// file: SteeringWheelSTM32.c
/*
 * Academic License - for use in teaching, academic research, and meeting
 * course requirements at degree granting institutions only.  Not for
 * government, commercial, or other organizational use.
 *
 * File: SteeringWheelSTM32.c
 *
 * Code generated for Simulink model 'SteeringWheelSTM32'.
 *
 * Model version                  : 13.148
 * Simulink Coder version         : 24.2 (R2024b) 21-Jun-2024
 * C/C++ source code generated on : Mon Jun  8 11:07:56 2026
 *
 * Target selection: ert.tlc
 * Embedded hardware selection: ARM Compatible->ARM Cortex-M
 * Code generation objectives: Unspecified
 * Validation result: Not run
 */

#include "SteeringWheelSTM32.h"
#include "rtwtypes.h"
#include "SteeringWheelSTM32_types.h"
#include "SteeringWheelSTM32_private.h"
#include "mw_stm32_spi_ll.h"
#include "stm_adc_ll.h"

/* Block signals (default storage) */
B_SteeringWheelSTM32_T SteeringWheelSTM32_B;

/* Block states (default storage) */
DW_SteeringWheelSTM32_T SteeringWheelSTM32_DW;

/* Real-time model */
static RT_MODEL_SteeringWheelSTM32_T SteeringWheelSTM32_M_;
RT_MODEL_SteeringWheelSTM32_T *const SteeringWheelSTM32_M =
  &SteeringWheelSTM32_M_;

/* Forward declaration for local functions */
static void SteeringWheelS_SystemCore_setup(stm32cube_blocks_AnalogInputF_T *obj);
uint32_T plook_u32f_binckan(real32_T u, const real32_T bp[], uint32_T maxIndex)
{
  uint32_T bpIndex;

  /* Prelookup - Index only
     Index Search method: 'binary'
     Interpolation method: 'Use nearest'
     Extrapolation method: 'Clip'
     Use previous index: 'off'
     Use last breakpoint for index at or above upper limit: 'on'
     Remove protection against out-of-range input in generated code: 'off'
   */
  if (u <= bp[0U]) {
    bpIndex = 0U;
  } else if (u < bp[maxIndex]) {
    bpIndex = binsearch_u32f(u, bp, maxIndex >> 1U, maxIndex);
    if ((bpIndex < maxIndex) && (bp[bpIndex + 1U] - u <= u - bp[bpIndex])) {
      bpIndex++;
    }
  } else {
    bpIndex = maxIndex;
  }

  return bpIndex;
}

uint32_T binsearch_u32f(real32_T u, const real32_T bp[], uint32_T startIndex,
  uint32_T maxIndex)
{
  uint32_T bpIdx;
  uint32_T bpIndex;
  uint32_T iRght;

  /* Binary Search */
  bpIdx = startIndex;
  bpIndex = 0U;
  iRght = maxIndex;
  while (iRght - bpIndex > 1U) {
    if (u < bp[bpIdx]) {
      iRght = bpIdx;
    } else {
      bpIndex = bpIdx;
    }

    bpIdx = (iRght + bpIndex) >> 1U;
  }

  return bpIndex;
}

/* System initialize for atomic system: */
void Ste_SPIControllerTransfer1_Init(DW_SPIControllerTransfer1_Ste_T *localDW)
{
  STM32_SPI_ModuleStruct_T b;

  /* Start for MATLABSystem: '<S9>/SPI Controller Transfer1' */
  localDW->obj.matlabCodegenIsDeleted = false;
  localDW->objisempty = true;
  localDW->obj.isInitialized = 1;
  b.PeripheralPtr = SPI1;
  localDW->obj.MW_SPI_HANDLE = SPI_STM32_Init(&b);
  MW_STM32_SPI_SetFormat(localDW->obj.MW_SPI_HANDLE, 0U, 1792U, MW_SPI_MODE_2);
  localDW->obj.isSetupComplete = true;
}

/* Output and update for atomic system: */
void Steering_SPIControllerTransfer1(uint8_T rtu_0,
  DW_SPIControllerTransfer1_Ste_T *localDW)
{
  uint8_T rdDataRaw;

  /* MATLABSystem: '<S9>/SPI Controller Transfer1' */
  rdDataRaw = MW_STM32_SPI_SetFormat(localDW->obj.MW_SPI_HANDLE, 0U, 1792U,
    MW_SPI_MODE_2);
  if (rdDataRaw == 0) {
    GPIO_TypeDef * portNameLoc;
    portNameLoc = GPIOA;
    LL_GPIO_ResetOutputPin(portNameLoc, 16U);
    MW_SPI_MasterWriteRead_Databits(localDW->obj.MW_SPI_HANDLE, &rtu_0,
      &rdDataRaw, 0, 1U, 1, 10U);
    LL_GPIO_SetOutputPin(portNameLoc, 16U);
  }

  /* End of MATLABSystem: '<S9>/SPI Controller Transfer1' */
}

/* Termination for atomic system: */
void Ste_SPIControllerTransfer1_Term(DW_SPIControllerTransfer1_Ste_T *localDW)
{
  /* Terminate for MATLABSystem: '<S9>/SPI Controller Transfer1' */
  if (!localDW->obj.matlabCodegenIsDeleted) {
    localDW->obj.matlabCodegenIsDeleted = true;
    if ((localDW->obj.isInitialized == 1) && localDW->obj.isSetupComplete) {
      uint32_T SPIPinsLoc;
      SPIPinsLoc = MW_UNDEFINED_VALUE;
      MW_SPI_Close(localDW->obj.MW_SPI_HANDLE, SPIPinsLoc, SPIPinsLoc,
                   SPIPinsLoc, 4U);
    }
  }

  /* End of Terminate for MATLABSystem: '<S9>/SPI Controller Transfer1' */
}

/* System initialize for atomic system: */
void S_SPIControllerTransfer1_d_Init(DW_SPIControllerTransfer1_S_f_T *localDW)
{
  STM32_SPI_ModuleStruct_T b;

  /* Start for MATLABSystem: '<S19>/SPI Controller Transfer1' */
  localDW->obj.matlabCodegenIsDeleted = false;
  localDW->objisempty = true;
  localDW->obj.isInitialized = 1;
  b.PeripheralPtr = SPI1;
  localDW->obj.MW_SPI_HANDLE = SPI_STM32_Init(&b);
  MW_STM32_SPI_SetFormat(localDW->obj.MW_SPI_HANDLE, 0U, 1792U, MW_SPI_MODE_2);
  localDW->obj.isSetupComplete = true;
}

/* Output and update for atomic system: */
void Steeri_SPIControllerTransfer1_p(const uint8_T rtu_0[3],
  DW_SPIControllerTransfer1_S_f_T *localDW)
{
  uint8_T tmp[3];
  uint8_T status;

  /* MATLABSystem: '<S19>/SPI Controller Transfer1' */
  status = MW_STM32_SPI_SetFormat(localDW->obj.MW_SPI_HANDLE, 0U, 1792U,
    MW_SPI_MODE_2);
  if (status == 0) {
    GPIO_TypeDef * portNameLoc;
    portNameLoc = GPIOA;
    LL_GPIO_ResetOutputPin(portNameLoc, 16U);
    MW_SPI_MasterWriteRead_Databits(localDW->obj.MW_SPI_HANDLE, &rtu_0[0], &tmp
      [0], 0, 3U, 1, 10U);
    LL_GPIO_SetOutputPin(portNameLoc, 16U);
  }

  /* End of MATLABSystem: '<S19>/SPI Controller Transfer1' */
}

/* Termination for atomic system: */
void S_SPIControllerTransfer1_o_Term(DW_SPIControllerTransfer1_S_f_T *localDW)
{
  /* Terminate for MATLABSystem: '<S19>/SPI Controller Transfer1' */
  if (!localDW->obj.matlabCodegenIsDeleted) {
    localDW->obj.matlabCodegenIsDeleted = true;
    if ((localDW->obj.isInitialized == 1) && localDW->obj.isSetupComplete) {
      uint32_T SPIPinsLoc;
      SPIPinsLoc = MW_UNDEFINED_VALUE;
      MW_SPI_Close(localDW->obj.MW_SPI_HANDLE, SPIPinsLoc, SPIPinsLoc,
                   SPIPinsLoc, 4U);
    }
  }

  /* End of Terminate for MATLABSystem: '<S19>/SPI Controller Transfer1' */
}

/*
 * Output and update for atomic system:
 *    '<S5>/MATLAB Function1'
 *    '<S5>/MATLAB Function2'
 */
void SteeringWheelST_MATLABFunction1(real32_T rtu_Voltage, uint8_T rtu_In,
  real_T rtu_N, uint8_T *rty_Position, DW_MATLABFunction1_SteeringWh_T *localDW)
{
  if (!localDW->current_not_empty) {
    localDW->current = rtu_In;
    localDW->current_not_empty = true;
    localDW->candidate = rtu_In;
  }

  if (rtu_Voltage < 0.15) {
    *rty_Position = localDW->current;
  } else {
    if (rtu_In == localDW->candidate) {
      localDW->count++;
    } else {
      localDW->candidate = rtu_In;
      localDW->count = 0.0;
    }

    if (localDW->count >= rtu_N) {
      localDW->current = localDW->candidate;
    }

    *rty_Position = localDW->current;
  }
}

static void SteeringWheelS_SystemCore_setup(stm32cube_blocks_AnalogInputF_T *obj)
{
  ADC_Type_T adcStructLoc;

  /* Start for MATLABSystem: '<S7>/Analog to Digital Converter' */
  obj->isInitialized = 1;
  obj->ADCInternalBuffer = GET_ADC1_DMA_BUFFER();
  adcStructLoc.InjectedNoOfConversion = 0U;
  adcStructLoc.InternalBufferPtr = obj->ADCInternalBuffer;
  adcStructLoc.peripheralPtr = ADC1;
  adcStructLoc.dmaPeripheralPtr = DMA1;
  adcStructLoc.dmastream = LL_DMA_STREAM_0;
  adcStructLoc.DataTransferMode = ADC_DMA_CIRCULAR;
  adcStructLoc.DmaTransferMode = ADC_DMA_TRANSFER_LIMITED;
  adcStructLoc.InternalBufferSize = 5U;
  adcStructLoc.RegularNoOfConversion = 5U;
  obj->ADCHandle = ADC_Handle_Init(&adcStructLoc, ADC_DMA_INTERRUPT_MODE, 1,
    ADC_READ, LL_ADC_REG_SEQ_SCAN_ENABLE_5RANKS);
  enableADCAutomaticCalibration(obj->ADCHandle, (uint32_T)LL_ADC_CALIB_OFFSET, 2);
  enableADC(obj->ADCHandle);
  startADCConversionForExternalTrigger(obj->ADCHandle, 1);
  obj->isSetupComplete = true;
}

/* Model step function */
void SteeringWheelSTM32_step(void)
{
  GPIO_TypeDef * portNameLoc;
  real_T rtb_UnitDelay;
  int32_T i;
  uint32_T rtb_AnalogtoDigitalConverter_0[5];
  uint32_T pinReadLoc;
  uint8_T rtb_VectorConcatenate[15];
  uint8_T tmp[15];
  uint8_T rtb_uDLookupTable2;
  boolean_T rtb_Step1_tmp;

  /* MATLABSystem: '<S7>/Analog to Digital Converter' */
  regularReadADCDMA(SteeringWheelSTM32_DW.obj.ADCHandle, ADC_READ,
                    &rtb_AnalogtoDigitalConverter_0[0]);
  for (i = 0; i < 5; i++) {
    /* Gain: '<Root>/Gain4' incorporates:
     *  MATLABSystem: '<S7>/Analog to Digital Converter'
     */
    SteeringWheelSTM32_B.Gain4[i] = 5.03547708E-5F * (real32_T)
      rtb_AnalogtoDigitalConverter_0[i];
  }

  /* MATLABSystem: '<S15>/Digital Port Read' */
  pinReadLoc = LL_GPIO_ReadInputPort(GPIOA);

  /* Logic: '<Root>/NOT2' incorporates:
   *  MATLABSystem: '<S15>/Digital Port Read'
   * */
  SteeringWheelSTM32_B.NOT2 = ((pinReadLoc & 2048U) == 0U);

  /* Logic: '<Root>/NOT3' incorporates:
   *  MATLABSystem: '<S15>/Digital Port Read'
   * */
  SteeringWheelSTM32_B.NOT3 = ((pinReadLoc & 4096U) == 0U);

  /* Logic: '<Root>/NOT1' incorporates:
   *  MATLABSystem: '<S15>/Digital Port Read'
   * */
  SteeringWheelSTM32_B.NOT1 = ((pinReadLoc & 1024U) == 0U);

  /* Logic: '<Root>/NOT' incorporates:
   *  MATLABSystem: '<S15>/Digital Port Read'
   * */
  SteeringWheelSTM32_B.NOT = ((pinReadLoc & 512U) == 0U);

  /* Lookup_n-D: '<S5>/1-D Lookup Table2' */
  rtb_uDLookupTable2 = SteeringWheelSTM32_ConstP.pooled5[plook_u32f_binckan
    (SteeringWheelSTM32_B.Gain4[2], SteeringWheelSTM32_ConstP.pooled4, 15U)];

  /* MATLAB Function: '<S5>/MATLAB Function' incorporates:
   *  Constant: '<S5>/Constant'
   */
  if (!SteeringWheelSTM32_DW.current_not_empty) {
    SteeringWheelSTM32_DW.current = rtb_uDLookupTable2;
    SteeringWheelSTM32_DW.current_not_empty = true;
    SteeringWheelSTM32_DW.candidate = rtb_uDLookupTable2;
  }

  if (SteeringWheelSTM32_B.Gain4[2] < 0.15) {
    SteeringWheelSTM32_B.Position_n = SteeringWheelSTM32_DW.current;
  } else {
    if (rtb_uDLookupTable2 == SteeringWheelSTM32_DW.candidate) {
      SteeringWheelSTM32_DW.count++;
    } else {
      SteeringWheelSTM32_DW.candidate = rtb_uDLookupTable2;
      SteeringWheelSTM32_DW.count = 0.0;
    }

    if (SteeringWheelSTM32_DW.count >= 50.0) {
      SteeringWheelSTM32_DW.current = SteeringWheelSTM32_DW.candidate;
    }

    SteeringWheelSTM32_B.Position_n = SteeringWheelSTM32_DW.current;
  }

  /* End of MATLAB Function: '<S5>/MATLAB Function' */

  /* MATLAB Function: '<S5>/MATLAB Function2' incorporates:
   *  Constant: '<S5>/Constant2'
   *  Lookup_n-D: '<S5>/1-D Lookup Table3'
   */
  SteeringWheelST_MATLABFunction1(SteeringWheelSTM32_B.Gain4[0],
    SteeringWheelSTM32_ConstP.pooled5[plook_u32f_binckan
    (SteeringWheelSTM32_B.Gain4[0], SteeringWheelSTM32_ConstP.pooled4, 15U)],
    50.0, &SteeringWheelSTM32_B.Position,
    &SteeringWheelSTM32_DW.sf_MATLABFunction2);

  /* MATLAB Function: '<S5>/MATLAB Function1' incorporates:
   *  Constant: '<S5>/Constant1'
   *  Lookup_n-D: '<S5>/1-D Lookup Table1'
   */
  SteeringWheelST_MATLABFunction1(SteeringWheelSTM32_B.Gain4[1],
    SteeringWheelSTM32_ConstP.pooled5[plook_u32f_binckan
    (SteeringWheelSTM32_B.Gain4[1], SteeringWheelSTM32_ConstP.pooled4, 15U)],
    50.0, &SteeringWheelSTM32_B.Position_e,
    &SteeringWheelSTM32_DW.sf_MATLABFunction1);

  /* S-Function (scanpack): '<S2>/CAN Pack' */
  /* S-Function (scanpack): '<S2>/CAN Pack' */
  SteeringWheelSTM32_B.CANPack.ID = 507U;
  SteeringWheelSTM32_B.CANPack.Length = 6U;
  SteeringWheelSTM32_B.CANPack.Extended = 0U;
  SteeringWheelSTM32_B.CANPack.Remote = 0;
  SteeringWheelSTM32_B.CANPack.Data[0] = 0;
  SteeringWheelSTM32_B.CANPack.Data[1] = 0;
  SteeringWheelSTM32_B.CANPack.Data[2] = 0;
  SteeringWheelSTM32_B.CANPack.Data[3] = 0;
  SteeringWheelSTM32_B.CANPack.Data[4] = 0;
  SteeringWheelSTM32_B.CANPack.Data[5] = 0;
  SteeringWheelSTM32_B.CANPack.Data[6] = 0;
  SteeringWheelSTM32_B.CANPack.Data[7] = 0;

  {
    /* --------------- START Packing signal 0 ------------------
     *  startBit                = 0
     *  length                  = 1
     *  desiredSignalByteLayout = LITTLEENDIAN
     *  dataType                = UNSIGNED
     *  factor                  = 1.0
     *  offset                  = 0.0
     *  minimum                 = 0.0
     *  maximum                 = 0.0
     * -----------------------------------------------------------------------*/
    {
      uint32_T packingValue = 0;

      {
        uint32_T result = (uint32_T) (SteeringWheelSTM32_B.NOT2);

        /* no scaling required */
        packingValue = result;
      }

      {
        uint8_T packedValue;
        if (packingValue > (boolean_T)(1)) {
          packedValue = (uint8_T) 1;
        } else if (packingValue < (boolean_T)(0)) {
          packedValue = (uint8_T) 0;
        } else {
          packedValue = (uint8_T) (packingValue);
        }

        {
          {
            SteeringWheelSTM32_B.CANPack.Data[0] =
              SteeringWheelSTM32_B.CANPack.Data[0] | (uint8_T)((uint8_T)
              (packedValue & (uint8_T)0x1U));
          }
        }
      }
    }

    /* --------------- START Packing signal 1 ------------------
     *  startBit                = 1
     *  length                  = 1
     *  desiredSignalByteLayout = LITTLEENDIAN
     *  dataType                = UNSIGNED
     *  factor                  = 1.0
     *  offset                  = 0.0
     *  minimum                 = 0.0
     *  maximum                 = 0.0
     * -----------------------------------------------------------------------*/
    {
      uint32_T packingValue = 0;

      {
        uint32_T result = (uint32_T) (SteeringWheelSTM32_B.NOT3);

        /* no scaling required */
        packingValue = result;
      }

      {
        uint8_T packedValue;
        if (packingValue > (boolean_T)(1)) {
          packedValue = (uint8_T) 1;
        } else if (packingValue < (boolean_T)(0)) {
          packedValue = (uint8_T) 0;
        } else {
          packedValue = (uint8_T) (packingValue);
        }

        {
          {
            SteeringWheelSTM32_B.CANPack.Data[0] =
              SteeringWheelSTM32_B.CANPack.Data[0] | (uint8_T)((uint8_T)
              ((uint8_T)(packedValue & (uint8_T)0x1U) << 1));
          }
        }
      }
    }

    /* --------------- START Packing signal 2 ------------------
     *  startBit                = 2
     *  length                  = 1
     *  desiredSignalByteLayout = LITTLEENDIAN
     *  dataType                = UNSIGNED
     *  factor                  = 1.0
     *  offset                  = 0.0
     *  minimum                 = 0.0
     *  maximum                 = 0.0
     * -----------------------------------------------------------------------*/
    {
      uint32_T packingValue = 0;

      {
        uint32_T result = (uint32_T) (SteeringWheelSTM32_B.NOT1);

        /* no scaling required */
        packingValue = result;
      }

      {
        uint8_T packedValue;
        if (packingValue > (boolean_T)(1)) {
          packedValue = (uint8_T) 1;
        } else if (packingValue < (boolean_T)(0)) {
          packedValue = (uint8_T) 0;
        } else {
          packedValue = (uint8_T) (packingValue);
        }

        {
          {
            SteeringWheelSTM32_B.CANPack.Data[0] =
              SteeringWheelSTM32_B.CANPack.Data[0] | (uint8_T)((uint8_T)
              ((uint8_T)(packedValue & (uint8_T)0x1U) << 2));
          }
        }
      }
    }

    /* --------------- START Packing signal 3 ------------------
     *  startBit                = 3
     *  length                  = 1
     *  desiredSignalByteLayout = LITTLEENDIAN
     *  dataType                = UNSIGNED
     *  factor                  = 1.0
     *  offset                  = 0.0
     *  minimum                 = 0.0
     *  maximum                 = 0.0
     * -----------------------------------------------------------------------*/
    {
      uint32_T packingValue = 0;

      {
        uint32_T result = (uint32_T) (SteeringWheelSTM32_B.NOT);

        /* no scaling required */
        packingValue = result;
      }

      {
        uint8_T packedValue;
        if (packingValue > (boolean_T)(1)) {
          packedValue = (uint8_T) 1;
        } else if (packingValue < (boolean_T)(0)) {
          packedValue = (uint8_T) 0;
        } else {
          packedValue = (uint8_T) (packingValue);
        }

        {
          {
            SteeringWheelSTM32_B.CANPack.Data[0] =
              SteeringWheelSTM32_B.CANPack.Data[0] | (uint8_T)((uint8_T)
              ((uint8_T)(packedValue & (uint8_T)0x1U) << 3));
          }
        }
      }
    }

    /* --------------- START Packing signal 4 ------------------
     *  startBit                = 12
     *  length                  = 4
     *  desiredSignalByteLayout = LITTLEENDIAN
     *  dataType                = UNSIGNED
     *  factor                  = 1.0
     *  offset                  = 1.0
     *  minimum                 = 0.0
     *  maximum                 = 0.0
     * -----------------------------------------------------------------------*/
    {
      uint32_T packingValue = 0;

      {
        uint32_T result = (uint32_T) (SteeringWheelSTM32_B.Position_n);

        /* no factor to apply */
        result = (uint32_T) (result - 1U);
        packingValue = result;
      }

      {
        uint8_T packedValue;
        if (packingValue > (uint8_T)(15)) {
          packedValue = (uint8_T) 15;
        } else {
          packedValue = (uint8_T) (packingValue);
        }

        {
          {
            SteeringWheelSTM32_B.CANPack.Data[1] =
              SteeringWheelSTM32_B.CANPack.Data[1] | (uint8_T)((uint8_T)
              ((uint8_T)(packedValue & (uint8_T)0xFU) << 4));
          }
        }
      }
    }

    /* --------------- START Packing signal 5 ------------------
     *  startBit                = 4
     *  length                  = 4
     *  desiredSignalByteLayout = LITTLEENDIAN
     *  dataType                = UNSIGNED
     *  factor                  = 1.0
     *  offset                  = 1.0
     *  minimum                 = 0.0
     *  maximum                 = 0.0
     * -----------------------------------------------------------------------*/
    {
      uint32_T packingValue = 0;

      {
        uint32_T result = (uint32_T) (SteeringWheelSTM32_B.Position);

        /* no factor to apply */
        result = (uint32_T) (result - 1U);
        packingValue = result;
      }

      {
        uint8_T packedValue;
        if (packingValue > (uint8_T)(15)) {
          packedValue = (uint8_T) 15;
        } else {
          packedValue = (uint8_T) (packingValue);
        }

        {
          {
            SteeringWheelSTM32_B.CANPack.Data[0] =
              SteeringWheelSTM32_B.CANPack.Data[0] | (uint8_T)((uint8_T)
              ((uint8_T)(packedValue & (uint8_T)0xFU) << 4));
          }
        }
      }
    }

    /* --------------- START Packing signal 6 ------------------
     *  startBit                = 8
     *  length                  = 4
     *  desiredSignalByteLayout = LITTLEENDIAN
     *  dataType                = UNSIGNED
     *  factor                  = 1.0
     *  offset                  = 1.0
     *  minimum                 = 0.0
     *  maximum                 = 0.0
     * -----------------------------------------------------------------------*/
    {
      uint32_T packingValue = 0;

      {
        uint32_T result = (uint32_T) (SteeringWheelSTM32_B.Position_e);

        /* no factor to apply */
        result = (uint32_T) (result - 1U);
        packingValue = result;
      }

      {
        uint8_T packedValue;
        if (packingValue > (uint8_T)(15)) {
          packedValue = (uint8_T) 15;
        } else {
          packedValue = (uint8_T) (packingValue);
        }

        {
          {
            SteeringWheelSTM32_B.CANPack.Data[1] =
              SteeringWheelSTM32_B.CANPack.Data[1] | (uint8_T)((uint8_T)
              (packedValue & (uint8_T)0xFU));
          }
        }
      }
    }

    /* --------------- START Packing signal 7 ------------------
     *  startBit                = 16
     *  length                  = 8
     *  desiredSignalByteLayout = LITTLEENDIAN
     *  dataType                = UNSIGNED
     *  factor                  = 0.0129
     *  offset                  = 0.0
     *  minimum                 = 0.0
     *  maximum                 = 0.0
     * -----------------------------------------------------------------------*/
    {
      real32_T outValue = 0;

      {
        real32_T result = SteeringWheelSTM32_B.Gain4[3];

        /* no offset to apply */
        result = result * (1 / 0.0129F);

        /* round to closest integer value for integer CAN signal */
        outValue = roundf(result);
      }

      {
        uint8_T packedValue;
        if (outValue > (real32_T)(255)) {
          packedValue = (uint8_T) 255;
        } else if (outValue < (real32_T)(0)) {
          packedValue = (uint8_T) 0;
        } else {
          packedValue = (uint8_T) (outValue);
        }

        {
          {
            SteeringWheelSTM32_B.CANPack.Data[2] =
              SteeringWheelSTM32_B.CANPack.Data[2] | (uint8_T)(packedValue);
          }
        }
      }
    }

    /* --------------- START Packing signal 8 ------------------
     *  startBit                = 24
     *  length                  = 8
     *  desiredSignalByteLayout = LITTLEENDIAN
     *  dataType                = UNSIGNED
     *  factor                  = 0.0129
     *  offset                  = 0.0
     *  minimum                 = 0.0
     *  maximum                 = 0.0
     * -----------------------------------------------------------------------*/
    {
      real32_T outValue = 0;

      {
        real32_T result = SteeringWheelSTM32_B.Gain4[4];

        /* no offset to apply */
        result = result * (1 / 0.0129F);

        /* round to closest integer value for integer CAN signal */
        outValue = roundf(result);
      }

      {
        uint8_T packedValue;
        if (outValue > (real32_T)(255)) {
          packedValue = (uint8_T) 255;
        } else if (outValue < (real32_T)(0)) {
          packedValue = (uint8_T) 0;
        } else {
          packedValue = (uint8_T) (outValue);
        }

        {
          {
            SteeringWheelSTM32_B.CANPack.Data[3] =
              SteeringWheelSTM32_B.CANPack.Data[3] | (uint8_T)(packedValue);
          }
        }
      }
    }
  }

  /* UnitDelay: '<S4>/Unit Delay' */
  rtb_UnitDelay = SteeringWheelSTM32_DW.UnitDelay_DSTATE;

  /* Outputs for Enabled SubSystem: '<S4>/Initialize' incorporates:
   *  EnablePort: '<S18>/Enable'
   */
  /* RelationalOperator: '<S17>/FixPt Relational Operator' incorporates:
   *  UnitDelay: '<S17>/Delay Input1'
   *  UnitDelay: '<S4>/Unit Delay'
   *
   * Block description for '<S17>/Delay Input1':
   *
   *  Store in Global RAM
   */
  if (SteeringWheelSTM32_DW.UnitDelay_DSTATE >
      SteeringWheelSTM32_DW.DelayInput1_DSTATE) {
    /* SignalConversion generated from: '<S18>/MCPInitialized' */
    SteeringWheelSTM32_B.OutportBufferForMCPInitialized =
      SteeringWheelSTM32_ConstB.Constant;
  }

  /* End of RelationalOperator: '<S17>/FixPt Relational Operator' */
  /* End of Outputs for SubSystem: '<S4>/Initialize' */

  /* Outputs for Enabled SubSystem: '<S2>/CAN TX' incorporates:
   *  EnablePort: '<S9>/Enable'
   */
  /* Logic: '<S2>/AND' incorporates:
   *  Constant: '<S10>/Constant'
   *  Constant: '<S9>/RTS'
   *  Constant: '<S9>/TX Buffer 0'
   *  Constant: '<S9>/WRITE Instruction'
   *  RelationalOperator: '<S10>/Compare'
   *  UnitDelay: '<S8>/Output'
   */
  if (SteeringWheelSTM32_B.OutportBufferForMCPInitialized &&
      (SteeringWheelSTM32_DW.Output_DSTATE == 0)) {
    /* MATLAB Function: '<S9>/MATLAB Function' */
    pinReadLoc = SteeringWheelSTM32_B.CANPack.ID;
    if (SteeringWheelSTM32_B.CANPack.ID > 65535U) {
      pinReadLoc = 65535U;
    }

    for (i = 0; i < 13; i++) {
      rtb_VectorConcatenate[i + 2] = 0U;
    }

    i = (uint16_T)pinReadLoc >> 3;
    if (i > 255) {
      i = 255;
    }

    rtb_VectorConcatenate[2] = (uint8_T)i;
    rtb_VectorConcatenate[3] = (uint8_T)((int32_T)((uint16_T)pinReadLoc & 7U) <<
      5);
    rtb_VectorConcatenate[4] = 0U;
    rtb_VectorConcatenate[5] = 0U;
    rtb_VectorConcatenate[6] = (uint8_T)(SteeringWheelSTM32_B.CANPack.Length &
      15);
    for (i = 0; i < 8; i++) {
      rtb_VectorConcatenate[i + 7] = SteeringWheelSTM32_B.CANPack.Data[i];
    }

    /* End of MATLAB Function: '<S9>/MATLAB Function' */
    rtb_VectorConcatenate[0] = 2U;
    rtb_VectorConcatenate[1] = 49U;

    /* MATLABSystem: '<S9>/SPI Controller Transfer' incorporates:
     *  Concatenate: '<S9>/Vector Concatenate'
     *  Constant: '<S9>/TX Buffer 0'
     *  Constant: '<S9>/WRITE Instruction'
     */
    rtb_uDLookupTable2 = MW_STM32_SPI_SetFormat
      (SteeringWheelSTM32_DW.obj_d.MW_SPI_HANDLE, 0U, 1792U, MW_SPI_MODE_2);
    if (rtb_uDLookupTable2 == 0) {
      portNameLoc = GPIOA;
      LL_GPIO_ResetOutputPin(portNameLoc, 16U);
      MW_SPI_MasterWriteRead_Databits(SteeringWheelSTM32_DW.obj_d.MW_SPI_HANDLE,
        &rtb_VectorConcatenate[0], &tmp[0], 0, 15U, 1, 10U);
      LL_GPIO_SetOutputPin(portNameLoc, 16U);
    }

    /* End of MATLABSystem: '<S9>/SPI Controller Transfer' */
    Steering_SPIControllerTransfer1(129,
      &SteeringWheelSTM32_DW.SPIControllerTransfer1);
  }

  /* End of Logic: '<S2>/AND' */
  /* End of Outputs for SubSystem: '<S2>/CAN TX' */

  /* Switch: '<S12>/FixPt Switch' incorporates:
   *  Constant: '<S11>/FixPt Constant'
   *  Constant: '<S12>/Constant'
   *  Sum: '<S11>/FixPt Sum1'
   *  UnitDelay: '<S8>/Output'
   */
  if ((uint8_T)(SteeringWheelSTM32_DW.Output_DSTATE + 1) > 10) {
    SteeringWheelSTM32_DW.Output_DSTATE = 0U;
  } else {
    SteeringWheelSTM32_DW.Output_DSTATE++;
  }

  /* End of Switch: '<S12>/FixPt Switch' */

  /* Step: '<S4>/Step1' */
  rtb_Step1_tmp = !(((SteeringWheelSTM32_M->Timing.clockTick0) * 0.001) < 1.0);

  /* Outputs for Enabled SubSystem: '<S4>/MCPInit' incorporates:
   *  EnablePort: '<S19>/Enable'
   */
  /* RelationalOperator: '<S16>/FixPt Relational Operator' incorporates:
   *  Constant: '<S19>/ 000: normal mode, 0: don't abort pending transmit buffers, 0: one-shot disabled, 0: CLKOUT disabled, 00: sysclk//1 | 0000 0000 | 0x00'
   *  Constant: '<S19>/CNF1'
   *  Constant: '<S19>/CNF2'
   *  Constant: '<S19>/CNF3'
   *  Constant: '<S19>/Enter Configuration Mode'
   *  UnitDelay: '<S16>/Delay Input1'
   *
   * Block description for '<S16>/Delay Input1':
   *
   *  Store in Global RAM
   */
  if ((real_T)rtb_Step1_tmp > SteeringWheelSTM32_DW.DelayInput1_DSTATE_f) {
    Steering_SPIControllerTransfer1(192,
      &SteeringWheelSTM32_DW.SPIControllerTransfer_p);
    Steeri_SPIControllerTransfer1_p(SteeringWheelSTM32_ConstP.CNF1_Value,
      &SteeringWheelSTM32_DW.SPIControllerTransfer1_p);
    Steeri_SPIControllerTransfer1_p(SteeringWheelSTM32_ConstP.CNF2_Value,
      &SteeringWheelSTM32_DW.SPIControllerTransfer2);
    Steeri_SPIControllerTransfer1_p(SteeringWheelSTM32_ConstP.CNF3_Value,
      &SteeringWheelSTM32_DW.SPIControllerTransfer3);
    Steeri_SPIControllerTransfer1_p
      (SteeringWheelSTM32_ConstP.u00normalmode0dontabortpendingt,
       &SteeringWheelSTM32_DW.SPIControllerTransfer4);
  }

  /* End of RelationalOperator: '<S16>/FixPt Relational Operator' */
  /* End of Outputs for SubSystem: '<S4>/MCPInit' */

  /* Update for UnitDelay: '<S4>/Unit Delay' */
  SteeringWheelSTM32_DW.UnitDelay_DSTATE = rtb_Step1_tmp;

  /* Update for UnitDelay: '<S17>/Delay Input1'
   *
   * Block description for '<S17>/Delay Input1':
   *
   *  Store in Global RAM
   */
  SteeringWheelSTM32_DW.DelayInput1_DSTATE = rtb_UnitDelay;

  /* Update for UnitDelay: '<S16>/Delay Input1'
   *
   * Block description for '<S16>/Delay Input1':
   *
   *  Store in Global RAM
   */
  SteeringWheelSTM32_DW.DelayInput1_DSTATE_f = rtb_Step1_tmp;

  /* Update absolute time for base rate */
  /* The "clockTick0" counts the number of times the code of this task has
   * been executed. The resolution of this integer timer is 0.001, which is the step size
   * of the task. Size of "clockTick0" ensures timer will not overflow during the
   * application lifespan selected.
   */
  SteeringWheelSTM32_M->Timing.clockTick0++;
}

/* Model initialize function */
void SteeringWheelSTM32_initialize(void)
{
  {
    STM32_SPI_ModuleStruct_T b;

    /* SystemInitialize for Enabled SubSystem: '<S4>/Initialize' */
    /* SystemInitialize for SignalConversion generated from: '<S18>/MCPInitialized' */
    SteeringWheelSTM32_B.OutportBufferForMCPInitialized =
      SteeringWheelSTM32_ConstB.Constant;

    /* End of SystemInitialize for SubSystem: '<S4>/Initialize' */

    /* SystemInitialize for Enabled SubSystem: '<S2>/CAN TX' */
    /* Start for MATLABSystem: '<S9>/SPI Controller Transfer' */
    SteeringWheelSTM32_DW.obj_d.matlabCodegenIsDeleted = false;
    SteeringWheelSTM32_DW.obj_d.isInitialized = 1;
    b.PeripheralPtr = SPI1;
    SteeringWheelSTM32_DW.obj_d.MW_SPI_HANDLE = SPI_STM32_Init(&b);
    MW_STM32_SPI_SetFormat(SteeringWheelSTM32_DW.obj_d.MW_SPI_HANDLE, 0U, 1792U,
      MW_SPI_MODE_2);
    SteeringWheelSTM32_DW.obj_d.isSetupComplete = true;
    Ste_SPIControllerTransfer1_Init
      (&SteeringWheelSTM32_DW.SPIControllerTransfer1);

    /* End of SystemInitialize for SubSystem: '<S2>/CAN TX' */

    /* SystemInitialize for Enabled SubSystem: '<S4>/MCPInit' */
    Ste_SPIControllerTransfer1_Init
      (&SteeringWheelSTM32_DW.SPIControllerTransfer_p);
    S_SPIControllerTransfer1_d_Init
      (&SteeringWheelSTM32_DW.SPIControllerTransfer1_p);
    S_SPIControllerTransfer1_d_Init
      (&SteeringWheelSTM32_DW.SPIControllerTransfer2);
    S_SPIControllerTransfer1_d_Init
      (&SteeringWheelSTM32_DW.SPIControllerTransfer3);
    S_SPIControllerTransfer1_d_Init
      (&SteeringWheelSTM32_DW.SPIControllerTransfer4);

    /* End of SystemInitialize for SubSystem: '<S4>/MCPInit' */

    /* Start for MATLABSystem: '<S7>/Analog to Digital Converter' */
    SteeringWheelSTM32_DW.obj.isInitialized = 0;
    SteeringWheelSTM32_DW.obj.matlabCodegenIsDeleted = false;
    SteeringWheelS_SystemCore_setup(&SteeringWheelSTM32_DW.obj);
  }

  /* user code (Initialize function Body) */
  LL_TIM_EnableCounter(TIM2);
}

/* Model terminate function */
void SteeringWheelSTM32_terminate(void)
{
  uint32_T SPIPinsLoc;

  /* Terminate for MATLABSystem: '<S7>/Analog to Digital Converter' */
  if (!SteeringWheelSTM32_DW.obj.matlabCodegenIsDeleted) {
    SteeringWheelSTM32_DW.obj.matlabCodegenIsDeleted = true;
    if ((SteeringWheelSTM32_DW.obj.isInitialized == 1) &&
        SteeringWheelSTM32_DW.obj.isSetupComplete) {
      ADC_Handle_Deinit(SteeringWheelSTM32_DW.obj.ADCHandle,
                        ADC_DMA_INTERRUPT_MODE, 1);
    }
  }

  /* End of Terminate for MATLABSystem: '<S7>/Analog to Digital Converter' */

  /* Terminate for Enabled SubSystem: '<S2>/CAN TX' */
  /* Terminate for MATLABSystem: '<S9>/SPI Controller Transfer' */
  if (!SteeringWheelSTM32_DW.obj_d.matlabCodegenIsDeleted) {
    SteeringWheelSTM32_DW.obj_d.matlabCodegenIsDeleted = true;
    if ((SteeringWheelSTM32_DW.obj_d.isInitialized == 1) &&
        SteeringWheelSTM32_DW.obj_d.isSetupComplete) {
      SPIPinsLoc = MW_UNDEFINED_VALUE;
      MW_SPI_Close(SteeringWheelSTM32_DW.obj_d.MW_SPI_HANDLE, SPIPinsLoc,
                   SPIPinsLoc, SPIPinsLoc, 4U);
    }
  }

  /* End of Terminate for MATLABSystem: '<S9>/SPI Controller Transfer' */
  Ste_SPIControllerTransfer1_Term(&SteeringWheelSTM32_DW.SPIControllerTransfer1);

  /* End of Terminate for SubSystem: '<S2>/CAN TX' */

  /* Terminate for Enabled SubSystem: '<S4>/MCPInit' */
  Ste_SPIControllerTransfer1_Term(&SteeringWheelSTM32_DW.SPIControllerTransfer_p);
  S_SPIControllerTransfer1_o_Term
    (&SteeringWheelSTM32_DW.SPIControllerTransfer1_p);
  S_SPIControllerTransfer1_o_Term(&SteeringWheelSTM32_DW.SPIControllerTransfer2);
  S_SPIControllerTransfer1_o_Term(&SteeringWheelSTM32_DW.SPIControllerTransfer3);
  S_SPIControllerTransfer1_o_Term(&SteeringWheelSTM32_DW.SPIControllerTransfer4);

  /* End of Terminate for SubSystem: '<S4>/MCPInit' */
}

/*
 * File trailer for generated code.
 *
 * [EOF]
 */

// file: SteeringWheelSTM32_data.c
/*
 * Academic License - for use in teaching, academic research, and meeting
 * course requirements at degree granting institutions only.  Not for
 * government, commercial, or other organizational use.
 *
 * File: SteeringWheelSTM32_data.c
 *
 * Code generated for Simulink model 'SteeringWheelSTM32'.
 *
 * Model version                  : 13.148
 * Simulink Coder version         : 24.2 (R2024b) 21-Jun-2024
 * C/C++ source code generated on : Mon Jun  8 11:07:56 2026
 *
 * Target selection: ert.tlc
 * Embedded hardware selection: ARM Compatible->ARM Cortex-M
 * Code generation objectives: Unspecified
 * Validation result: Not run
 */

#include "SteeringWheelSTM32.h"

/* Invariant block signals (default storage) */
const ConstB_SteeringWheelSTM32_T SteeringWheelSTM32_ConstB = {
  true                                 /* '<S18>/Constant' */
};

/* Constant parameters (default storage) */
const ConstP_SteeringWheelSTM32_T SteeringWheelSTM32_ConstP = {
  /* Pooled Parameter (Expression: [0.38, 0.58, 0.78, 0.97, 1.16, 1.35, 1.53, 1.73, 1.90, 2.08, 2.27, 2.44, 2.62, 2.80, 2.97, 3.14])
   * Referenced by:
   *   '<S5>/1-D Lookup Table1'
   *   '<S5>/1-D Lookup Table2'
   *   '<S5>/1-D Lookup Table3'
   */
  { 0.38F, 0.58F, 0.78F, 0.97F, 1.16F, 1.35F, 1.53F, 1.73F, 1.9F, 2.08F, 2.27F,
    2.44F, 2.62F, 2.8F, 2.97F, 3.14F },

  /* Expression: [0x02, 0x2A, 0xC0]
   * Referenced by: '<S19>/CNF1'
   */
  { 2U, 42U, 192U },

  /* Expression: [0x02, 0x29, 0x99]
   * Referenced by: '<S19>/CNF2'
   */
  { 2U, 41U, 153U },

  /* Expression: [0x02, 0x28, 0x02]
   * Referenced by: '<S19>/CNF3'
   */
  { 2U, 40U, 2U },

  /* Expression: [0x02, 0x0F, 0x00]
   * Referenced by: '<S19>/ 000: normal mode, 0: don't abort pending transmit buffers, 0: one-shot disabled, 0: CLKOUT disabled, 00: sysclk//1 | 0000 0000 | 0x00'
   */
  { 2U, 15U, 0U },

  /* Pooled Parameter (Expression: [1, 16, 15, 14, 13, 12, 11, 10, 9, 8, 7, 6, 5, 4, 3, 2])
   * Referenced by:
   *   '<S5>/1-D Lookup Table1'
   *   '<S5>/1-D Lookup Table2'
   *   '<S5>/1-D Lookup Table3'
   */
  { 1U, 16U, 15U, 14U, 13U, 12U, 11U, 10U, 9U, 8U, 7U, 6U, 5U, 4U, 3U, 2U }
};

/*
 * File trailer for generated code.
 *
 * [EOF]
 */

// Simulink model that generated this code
simulink model "SteeringWheelSTM32"  (R2024b)
settings: Solver=FixedStepDiscrete  StartTime=0.0  StopTime=1  FixedStep=0.001  RelTol=1e-3  EnableMultiTasking=on
libraries: stm32blockslib x7, simulink x4, stm32h7xxblockslib x1, canmsglib x1, stm32f4xxblockslib x1

== system SteeringWheelSTM32 ==
  Analog to Digital Converter : stm32h7xxblockslib/Analog to Digital Converter  ADCModule=ADC1  ConversionGroup=Regular  TriggerMode=Read results only  NumberOfConversions=5  EnableBufferConv=on  BufferLength=1  OutputStatus=off  SampleTime=-1  EnableSimPort=off  hoistedMaskSrc=ECSoC/ECSimCodegen/Analog to Digital Converter
  CAN Tx : Subsystem
  Demux : Demux  Outputs=5
  Demux1 : Demux
  Digital Port Read : stm32f4xxblockslib/Digital Port Read  PortName=GPIOA  PinNumber=[9, 10, 11, 12]  ReadOperation=on  IOAsArray=on  SampleTime=-1  EnableSimPort=off  hoistedMaskSrc=ECSoC/ECSimCodegen/Digital Port Read
  Gain4 : Gain  Gain=3.3/65535  OutDataTypeStr=single
  NOT{,1..3} (4 alike) : Logic  Operator=NOT  IconShape=distinctive  AllPortsSameDT=off  OutDataTypeStr=boolean
  Subsystem : Subsystem
  Voltage To Position : Subsystem
  wires:
  Demux1/3 -> NOT2/1
  Demux1/4 -> NOT3/1
  Demux1/2 -> NOT1/1
  Demux1/1 -> NOT/1
  [VRotary1] -> Voltage To Position/1(VRotary1)
  [VRotary2] -> Voltage To Position/2(VRotary2)
  [VRotary3] -> Voltage To Position/3(VRotary3)
  Voltage To Position/1(NRotary1) -> [NPageSelectRotary]
  Voltage To Position/2(NRotary2) -> [NParameterSelectRotary]
  Voltage To Position/3(NRotary3) -> [NEventModeRotary]
  [NEventModeRotary] -> CAN Tx/6(NEventModeRotary)
  [NPageSelectRotary] -> CAN Tx/7(NPageSelectRotary)
  [NParameterSelectRotary] -> CAN Tx/8(NParameterSelectRotary)
  [VRegen1] -> CAN Tx/9(VRegenPaddle1)
  [VRegen2] -> CAN Tx/10(VRegenPaddle2)
  [BSteeringWheelButton1] -> CAN Tx/2(BSteeringWheelButton1)
  [BSteeringWheelButton2] -> CAN Tx/3(BSteeringWheelButton2)
  [BSteeringWheelButton3] -> CAN Tx/4(BSteeringWheelButton3)
  [BSteeringWheelButton4] -> CAN Tx/5(BSteeringWheelButton4)
  Digital Port Read/1 -> Demux1/1
  NOT/1 -> [BSteeringWheelButton4]
  NOT1/1 -> [BSteeringWheelButton3]
  NOT2/1 -> [BSteeringWheelButton1]
  NOT3/1 -> [BSteeringWheelButton2]
  Demux/1 -> [VRotary1]
  Demux/2 -> [VRotary2]
  Demux/3 -> [VRotary3]
  Demux/4 -> [VRegen1]
  Demux/5 -> [VRegen2]
  Gain4/1 -> Demux/1
  Analog to Digital Converter/1 -> Gain4/1
  [MCPInitialized] -> CAN Tx/1(MCPInitialized)
  Subsystem/1(MCPInitialized) -> [MCPInitialized]

== system SteeringWheelSTM32/CAN Tx ==
  MCPInitialized : Inport
  BSteeringWheelButton1 : Inport  Port=2
  BSteeringWheelButton2 : Inport  Port=3
  BSteeringWheelButton3 : Inport  Port=4
  BSteeringWheelButton4 : Inport  Port=5
  NEventModeRotary : Inport  Port=6
  NPageSelectRotary : Inport  Port=7
  NParameterSelectRotary : Inport  Port=8
  VRegenPaddle1 : Inport  Port=9
  VRegenPaddle2 : Inport  Port=10
  AND : Logic  IconShape=distinctive  AllPortsSameDT=off  OutDataTypeStr=boolean
  CAN Message Period : simulink/Sources/Counter Limited  uplimit=10  tsamp=-1
  CAN Pack : canmsglib/CAN Pack  CANdbFile=C:\Users\William\Downloads\SteeringWheelSTM32\STW_Database.dbc  MsgList=SteeringWheelTest  MsgName=SteeringWheelTest  MsgIDType=Standard (11-bit identifier)  MsgIdentifier=507  CANIDInput=off  MsgLength=6  Remote=off  ApplyMinMax=off  BusOutput=on  SignalInfo={'BSteeringWheelButton1','0','1','LE','unsigned','Standard','0','1','0','0','1';'BSteeringWheelButton2','1','1','LE','unsigned','Standard','0','1','0','0','1';'BSteeringWheelButton3','2','1','LE','unsigned','Standard','0','1','0','0','1';'BSteeringWheelButton4','3','1','LE','unsigned','Standard','0','1','0','0','1';'NEventModeRotary','12','4','LE','unsigned','Standard','0','1','1','1','16';'NPageSelectRotary','4','4','LE','unsigned','Standard','0','1','1','1','16';'NParameterSelectRotary','8','4','LE','unsigned','Standard','0','1','1','1','16';'VRegenPaddle1','16','8','LE','unsigned','Standard','0','0.0129','0','0','3.2895';'VRegenPaddle2','24','8','LE','unsigned','Standard','0','0.0129','0','0','3.2895'}
  CAN TX : Subsystem  TreatAsAtomicUnit=on
  Compare To Constant : simulink/Logic and Bit Operations/Compare To Constant  relop===  const=0  OutDataTypeStr=boolean
  wires:
  AND/1 -> CAN TX/Enable
  CAN Pack/1 -> CAN TX/1(MessageData)
  CAN Message Period/1 -> Compare To Constant/1
  MCPInitialized/1 -> AND/1
  Compare To Constant/1 -> AND/2
  BSteeringWheelButton1/1 -> CAN Pack/1
  BSteeringWheelButton4/1 -> CAN Pack/4
  BSteeringWheelButton3/1 -> CAN Pack/3
  BSteeringWheelButton2/1 -> CAN Pack/2
  NEventModeRotary/1 -> CAN Pack/5
  NPageSelectRotary/1 -> CAN Pack/6
  NParameterSelectRotary/1 -> CAN Pack/7
  VRegenPaddle1/1 -> CAN Pack/8
  VRegenPaddle2/1 -> CAN Pack/9

== system SteeringWheelSTM32/Subsystem ==
  Detect Increase : simulink/Logic and Bit Operations/Detect Increase  vinit=0.0  OutDataTypeStr=boolean
  Detect Increase1 : simulink/Logic and Bit Operations/Detect Increase  vinit=0.0  OutDataTypeStr=boolean
  Initialize : Subsystem  TreatAsAtomicUnit=on
  MCPInit : Subsystem  TreatAsAtomicUnit=on
  Step1 : Step
  Step2 : Step
  Unit Delay : UnitDelay  SampleTime=-1  HasFrameUpgradeWarning=on
  MCPInitialized : Outport
  wires:
  Step1/1 -> Detect Increase/1
  Unit Delay/1 -> Detect Increase1/1
  Detect Increase1/1 -> Initialize/Enable
  Detect Increase/1 -> MCPInit/Enable
  Step2/1 -> Unit Delay/1
  Initialize/1(MCPInitialized) -> MCPInitialized/1

== system SteeringWheelSTM32/Voltage To Position ==
  VRotary1 : Inport  OutDataTypeStr=single
  VRotary2 : Inport  Port=2  OutDataTypeStr=single
  VRotary3 : Inport  Port=3  OutDataTypeStr=single
  1-D Lookup Table1 : Lookup_n-D  NumberOfTableDimensions=1  BreakpointsForDimension1=[0.38, 0.58, 0.78, 0.97, 1.16, 1.35, 1.53, 1.73, 1.90, 2.08, 2.27, 2.44, 2.62, 2.80, 2.97, 3.14]  Table=[1, 16, 15, 14, 13, 12, 11, 10, 9, 8, 7, 6, 5, 4, 3, 2]  InterpMethod=Nearest  InternalRulePriority=Speed  OutDataTypeStr=uint8  RndMeth=Simplest
  1-D Lookup Table2 : Lookup_n-D  NumberOfTableDimensions=1  BreakpointsForDimension1=[0.38, 0.58, 0.78, 0.97, 1.16, 1.35, 1.53, 1.73, 1.90, 2.08, 2.27, 2.44, 2.62, 2.80, 2.97, 3.14]  Table=[1, 16, 15, 14, 13, 12, 11, 10, 9, 8, 7, 6, 5, 4, 3, 2]  InterpMethod=Nearest  InternalRulePriority=Speed  OutDataTypeStr=uint8  RndMeth=Simplest
  1-D Lookup Table3 : Lookup_n-D  NumberOfTableDimensions=1  BreakpointsForDimension1=[0.38, 0.58, 0.78, 0.97, 1.16, 1.35, 1.53, 1.73, 1.90, 2.08, 2.27, 2.44, 2.62, 2.80, 2.97, 3.14]  Table=[1, 16, 15, 14, 13, 12, 11, 10, 9, 8, 7, 6, 5, 4, 3, 2]  InterpMethod=Nearest  InternalRulePriority=Speed  OutDataTypeStr=uint8  RndMeth=Simplest
  Constant : Constant  Value=50
  Constant1 : Constant  Value=50
  Constant2 : Constant  Value=50
  MATLAB Function : MATLAB Function  TreatAsAtomicUnit=on
  MATLAB Function1 : MATLAB Function  TreatAsAtomicUnit=on
  MATLAB Function2 : MATLAB Function  TreatAsAtomicUnit=on
  NRotary1 : Outport  OutDataTypeStr=uint8
  NRotary2 : Outport  Port=2  OutDataTypeStr=uint8
  NRotary3 : Outport  Port=3  OutDataTypeStr=uint8
  wires:
  VRotary3/1 -> MATLAB Function/1(Voltage), 1-D Lookup Table2/1
  Constant/1 -> MATLAB Function/3(N)
  MATLAB Function/1(Position) -> NRotary3/1
  MATLAB Function1/1(Position) -> NRotary2/1
  VRotary2/1 -> MATLAB Function1/1(Voltage), 1-D Lookup Table1/1
  Constant1/1 -> MATLAB Function1/3(N)
  1-D Lookup Table1/1 -> MATLAB Function1/2(In)
  MATLAB Function2/1(Position) -> NRotary1/1
  VRotary1/1 -> MATLAB Function2/1(Voltage), 1-D Lookup Table3/1
  Constant2/1 -> MATLAB Function2/3(N)
  1-D Lookup Table3/1 -> MATLAB Function2/2(In)
  1-D Lookup Table2/1 -> MATLAB Function/2(In)

== system SteeringWheelSTM32/CAN Tx/CAN TX ==
  MessageData : Inport
  Enable : EnablePort
  Bus Selector : BusSelector  OutputSignals=ID,Length,Data
  MATLAB Function : MATLAB Function  TreatAsAtomicUnit=on
  RTS : Constant  Value=0x81  OutDataTypeStr=uint8  SampleTime=-1
  SPI Controller Transfer : stm32blockslib/SPI Controller Transfer  Priority=1  SPIModuleSelect=SPI1  ClockPolarity=Low  ClockPhase=1 Edge  SPIModule=uint32(0)  Mode=Master  BusSpeed=uint32(1000000)  FirstBitToTransfer=Most significant bit (MSB)  ClockMode=0  BlockFunction=Transfer  EnableRegisterAddress=off  RegisterAddress=0  OutputDataType=uint8  OutputDataLength=1  OutputStatus=off  BlockingMode=on  Timeout=0.01  DataBits=8  UseCustomSSPin=Explicit GPIO calls  ActiveLowSSPin=Active low  Port_Select=GPIOA  Pin=4
  SPI Controller Transfer1 : stm32blockslib/SPI Controller Transfer  Priority=5  SPIModuleSelect=SPI1  ClockPolarity=Low  ClockPhase=1 Edge  SPIModule=uint32(0)  Mode=Master  BusSpeed=uint32(1000000)  FirstBitToTransfer=Most significant bit (MSB)  ClockMode=0  BlockFunction=Transfer  EnableRegisterAddress=off  RegisterAddress=0  OutputDataType=uint8  OutputDataLength=1  OutputStatus=off  BlockingMode=on  Timeout=0.01  DataBits=8  UseCustomSSPin=Explicit GPIO calls  ActiveLowSSPin=Active low  Port_Select=GPIOA  Pin=4
  TX Buffer 0 : Constant  Value=0x31  OutDataTypeStr=uint8  SampleTime=-1
  Terminator : Terminator
  Terminator1 : Terminator
  Vector Concatenate : Concatenate  NumInputs=3
  WRITE Instruction : Constant  Value=0x02  OutDataTypeStr=uint8  SampleTime=-1
  wires:
  SPI Controller Transfer1/1 -> Terminator1/1
  Bus Selector/2 -> MATLAB Function/2(Length)  "<Length>"
  Bus Selector/1 -> MATLAB Function/1(ID)  "<ID>"
  MATLAB Function/1(CANVector) -> Vector Concatenate/3
  TX Buffer 0/1 -> Vector Concatenate/2
  Bus Selector/3 -> MATLAB Function/3(Data)  "<Data>"
  MessageData/1 -> Bus Selector/1
  WRITE Instruction/1 -> Vector Concatenate/1
  SPI Controller Transfer/1 -> Terminator/1
  Vector Concatenate/1 -> SPI Controller Transfer/1
  RTS/1 -> SPI Controller Transfer1/1

== system SteeringWheelSTM32/Subsystem/Initialize ==
  Enable : EnablePort
  Constant : Constant  OutDataTypeStr=boolean
  MCPInitialized : Outport
  wires:
  Constant/1 -> MCPInitialized/1

== system SteeringWheelSTM32/Subsystem/MCPInit ==
  note: 0x02, 0x2A, 0x40 | 0x02, 0x29, 0x9B | 0x02, 0x28, 0x83 | 0x02, 0x0F, 0x14
  Enable : EnablePort
  " 000: normal mode, 0: don't abort pending transmit buffers, 0: one-shot disabled, 0: CLKOUT disabled, 00: sysclk/1 | 0000 0000 | 0x00" : Constant  Value=[0x02, 0x0F, 0x00]  OutDataTypeStr=uint8
  CNF1 : Constant  Value=[0x02, 0x2A, 0xC0]  OutDataTypeStr=uint8
  CNF2 : Constant  Value=[0x02, 0x29, 0x99]  OutDataTypeStr=uint8
  CNF3 : Constant  Value=[0x02, 0x28, 0x02]  OutDataTypeStr=uint8
  Enter Configuration Mode : Constant  Value=0xc0  OutDataTypeStr=uint8
  SPI Controller Transfer : stm32blockslib/SPI Controller Transfer  Priority=4  SPIModuleSelect=SPI1  ClockPolarity=Low  ClockPhase=1 Edge  SPIModule=uint32(0)  Mode=Master  BusSpeed=uint32(1000000)  FirstBitToTransfer=Most significant bit (MSB)  ClockMode=0  BlockFunction=Transfer  EnableRegisterAddress=off  RegisterAddress=0  OutputDataType=uint8  OutputDataLength=1  OutputStatus=off  BlockingMode=on  Timeout=0.01  DataBits=8  UseCustomSSPin=Explicit GPIO calls  ActiveLowSSPin=Active low  Port_Select=GPIOA  Pin=4
  SPI Controller Transfer1 : stm32blockslib/SPI Controller Transfer  Priority=5  SPIModuleSelect=SPI1  ClockPolarity=Low  ClockPhase=1 Edge  SPIModule=uint32(0)  Mode=Master  BusSpeed=uint32(1000000)  FirstBitToTransfer=Most significant bit (MSB)  ClockMode=0  BlockFunction=Transfer  EnableRegisterAddress=off  RegisterAddress=0  OutputDataType=uint8  OutputDataLength=1  OutputStatus=off  BlockingMode=on  Timeout=0.01  DataBits=8  UseCustomSSPin=Explicit GPIO calls  ActiveLowSSPin=Active low  Port_Select=GPIOA  Pin=4
  SPI Controller Transfer2 : stm32blockslib/SPI Controller Transfer  Priority=6  SPIModuleSelect=SPI1  ClockPolarity=Low  ClockPhase=1 Edge  SPIModule=uint32(0)  Mode=Master  BusSpeed=uint32(1000000)  FirstBitToTransfer=Most significant bit (MSB)  ClockMode=0  BlockFunction=Transfer  EnableRegisterAddress=off  RegisterAddress=0  OutputDataType=uint8  OutputDataLength=1  OutputStatus=off  BlockingMode=on  Timeout=0.01  DataBits=8  UseCustomSSPin=Explicit GPIO calls  ActiveLowSSPin=Active low  Port_Select=GPIOA  Pin=4
  SPI Controller Transfer3 : stm32blockslib/SPI Controller Transfer  Priority=7  SPIModuleSelect=SPI1  ClockPolarity=Low  ClockPhase=1 Edge  SPIModule=uint32(0)  Mode=Master  BusSpeed=uint32(1000000)  FirstBitToTransfer=Most significant bit (MSB)  ClockMode=0  BlockFunction=Transfer  EnableRegisterAddress=off  RegisterAddress=0  OutputDataType=uint8  OutputDataLength=1  OutputStatus=off  BlockingMode=on  Timeout=0.01  DataBits=8  UseCustomSSPin=Explicit GPIO calls  ActiveLowSSPin=Active low  Port_Select=GPIOA  Pin=4
  SPI Controller Transfer4 : stm32blockslib/SPI Controller Transfer  Priority=8  SPIModuleSelect=SPI1  ClockPolarity=Low  ClockPhase=1 Edge  SPIModule=uint32(0)  Mode=Master  BusSpeed=uint32(1000000)  FirstBitToTransfer=Most significant bit (MSB)  ClockMode=0  BlockFunction=Transfer  EnableRegisterAddress=off  RegisterAddress=0  OutputDataType=uint8  OutputDataLength=1  OutputStatus=off  BlockingMode=on  Timeout=0.01  DataBits=8  UseCustomSSPin=Explicit GPIO calls  ActiveLowSSPin=Active low  Port_Select=GPIOA  Pin=4
  Terminator{,1..4} (5 alike) : Terminator
  wires:
  SPI Controller Transfer/1 -> Terminator/1
  Enter Configuration Mode/1 -> SPI Controller Transfer/1
  CNF1/1 -> SPI Controller Transfer1/1
  SPI Controller Transfer1/1 -> Terminator1/1
  CNF2/1 -> SPI Controller Transfer2/1
  SPI Controller Transfer2/1 -> Terminator2/1
  CNF3/1 -> SPI Controller Transfer3/1
  SPI Controller Transfer3/1 -> Terminator3/1
  " 000: normal mode, 0: don't abort pending transmit buffers, 0: one-shot disabled, 0: CLKOUT disabled, 00: sysclk/1 | 0000 0000 | 0x00"/1 -> SPI Controller Transfer4/1
  SPI Controller Transfer4/1 -> Terminator4/1

== matlab function SteeringWheelSTM32/CAN Tx/CAN TX/MATLAB Function ==
function CANVector = ConvertToVector(ID, Length, Data)
    %#codegen
    id_u16 = uint16(ID);
    len_u8 = uint8(Length);

    CANVector = zeros(1, 13, 'uint8');  % 13 bytes only — no instruction

    CANVector(1) = uint8(bitshift(id_u16, -3));              % SIDH: ID[10:3]
    CANVector(2) = uint8(bitshift(bitand(id_u16, uint16(7)), 5)); % SIDL: ID[2:0]<<5, EXIDE=0
    CANVector(3) = uint8(0);   % EID8 unused
    CANVector(4) = uint8(0);   % EID0 unused
    CANVector(5) = bitand(len_u8, uint8(15));  % DLC
    for i = 1:8
        CANVector(5+i) = uint8(Data(i));
    end

== matlab function SteeringWheelSTM32/Voltage To Position/MATLAB Function ==
function Position = Debounce(Voltage, In, N)
    persistent current candidate count;
    
    if isempty(current)
        current = In;
        candidate = In;
        count = 0;
    end
    
    % IGNORE reading entirely if voltage is near 0 (in transition)
    if Voltage < 0.15
        Position = current;  % just hold, don't even consider updating
        return;
    end
    
    if In == candidate
        count = count + 1;
    else
        candidate = In;
        count = 0;
    end
    
    if count >= N
        current = candidate;
    end
    
    Position = current;
end

== matlab function SteeringWheelSTM32/Voltage To Position/MATLAB Function1 ==
function Position = Debounce(Voltage, In, N)
    persistent current candidate count;
    
    if isempty(current)
        current = In;
        candidate = In;
        count = 0;
    end
    
    % IGNORE reading entirely if voltage is near 0 (in transition)
    if Voltage < 0.15
        Position = current;  % just hold, don't even consider updating
        return;
    end
    
    if In == candidate
        count = count + 1;
    else
        candidate = In;
        count = 0;
    end
    
    if count >= N
        current = candidate;
    end
    
    Position = current;
end

== matlab function SteeringWheelSTM32/Voltage To Position/MATLAB Function2 ==
function Position = Debounce(Voltage, In, N)
    persistent current candidate count;
    
    if isempty(current)
        current = In;
        candidate = In;
        count = 0;
    end
    
    % IGNORE reading entirely if voltage is near 0 (in transition)
    if Voltage < 0.15
        Position = current;  % just hold, don't even consider updating
        return;
    end
    
    if In == candidate
        count = count + 1;
    else
        candidate = In;
        count = 0;
    end
    
    if count >= N
        current = candidate;
    end
    
    Position = current;
end
